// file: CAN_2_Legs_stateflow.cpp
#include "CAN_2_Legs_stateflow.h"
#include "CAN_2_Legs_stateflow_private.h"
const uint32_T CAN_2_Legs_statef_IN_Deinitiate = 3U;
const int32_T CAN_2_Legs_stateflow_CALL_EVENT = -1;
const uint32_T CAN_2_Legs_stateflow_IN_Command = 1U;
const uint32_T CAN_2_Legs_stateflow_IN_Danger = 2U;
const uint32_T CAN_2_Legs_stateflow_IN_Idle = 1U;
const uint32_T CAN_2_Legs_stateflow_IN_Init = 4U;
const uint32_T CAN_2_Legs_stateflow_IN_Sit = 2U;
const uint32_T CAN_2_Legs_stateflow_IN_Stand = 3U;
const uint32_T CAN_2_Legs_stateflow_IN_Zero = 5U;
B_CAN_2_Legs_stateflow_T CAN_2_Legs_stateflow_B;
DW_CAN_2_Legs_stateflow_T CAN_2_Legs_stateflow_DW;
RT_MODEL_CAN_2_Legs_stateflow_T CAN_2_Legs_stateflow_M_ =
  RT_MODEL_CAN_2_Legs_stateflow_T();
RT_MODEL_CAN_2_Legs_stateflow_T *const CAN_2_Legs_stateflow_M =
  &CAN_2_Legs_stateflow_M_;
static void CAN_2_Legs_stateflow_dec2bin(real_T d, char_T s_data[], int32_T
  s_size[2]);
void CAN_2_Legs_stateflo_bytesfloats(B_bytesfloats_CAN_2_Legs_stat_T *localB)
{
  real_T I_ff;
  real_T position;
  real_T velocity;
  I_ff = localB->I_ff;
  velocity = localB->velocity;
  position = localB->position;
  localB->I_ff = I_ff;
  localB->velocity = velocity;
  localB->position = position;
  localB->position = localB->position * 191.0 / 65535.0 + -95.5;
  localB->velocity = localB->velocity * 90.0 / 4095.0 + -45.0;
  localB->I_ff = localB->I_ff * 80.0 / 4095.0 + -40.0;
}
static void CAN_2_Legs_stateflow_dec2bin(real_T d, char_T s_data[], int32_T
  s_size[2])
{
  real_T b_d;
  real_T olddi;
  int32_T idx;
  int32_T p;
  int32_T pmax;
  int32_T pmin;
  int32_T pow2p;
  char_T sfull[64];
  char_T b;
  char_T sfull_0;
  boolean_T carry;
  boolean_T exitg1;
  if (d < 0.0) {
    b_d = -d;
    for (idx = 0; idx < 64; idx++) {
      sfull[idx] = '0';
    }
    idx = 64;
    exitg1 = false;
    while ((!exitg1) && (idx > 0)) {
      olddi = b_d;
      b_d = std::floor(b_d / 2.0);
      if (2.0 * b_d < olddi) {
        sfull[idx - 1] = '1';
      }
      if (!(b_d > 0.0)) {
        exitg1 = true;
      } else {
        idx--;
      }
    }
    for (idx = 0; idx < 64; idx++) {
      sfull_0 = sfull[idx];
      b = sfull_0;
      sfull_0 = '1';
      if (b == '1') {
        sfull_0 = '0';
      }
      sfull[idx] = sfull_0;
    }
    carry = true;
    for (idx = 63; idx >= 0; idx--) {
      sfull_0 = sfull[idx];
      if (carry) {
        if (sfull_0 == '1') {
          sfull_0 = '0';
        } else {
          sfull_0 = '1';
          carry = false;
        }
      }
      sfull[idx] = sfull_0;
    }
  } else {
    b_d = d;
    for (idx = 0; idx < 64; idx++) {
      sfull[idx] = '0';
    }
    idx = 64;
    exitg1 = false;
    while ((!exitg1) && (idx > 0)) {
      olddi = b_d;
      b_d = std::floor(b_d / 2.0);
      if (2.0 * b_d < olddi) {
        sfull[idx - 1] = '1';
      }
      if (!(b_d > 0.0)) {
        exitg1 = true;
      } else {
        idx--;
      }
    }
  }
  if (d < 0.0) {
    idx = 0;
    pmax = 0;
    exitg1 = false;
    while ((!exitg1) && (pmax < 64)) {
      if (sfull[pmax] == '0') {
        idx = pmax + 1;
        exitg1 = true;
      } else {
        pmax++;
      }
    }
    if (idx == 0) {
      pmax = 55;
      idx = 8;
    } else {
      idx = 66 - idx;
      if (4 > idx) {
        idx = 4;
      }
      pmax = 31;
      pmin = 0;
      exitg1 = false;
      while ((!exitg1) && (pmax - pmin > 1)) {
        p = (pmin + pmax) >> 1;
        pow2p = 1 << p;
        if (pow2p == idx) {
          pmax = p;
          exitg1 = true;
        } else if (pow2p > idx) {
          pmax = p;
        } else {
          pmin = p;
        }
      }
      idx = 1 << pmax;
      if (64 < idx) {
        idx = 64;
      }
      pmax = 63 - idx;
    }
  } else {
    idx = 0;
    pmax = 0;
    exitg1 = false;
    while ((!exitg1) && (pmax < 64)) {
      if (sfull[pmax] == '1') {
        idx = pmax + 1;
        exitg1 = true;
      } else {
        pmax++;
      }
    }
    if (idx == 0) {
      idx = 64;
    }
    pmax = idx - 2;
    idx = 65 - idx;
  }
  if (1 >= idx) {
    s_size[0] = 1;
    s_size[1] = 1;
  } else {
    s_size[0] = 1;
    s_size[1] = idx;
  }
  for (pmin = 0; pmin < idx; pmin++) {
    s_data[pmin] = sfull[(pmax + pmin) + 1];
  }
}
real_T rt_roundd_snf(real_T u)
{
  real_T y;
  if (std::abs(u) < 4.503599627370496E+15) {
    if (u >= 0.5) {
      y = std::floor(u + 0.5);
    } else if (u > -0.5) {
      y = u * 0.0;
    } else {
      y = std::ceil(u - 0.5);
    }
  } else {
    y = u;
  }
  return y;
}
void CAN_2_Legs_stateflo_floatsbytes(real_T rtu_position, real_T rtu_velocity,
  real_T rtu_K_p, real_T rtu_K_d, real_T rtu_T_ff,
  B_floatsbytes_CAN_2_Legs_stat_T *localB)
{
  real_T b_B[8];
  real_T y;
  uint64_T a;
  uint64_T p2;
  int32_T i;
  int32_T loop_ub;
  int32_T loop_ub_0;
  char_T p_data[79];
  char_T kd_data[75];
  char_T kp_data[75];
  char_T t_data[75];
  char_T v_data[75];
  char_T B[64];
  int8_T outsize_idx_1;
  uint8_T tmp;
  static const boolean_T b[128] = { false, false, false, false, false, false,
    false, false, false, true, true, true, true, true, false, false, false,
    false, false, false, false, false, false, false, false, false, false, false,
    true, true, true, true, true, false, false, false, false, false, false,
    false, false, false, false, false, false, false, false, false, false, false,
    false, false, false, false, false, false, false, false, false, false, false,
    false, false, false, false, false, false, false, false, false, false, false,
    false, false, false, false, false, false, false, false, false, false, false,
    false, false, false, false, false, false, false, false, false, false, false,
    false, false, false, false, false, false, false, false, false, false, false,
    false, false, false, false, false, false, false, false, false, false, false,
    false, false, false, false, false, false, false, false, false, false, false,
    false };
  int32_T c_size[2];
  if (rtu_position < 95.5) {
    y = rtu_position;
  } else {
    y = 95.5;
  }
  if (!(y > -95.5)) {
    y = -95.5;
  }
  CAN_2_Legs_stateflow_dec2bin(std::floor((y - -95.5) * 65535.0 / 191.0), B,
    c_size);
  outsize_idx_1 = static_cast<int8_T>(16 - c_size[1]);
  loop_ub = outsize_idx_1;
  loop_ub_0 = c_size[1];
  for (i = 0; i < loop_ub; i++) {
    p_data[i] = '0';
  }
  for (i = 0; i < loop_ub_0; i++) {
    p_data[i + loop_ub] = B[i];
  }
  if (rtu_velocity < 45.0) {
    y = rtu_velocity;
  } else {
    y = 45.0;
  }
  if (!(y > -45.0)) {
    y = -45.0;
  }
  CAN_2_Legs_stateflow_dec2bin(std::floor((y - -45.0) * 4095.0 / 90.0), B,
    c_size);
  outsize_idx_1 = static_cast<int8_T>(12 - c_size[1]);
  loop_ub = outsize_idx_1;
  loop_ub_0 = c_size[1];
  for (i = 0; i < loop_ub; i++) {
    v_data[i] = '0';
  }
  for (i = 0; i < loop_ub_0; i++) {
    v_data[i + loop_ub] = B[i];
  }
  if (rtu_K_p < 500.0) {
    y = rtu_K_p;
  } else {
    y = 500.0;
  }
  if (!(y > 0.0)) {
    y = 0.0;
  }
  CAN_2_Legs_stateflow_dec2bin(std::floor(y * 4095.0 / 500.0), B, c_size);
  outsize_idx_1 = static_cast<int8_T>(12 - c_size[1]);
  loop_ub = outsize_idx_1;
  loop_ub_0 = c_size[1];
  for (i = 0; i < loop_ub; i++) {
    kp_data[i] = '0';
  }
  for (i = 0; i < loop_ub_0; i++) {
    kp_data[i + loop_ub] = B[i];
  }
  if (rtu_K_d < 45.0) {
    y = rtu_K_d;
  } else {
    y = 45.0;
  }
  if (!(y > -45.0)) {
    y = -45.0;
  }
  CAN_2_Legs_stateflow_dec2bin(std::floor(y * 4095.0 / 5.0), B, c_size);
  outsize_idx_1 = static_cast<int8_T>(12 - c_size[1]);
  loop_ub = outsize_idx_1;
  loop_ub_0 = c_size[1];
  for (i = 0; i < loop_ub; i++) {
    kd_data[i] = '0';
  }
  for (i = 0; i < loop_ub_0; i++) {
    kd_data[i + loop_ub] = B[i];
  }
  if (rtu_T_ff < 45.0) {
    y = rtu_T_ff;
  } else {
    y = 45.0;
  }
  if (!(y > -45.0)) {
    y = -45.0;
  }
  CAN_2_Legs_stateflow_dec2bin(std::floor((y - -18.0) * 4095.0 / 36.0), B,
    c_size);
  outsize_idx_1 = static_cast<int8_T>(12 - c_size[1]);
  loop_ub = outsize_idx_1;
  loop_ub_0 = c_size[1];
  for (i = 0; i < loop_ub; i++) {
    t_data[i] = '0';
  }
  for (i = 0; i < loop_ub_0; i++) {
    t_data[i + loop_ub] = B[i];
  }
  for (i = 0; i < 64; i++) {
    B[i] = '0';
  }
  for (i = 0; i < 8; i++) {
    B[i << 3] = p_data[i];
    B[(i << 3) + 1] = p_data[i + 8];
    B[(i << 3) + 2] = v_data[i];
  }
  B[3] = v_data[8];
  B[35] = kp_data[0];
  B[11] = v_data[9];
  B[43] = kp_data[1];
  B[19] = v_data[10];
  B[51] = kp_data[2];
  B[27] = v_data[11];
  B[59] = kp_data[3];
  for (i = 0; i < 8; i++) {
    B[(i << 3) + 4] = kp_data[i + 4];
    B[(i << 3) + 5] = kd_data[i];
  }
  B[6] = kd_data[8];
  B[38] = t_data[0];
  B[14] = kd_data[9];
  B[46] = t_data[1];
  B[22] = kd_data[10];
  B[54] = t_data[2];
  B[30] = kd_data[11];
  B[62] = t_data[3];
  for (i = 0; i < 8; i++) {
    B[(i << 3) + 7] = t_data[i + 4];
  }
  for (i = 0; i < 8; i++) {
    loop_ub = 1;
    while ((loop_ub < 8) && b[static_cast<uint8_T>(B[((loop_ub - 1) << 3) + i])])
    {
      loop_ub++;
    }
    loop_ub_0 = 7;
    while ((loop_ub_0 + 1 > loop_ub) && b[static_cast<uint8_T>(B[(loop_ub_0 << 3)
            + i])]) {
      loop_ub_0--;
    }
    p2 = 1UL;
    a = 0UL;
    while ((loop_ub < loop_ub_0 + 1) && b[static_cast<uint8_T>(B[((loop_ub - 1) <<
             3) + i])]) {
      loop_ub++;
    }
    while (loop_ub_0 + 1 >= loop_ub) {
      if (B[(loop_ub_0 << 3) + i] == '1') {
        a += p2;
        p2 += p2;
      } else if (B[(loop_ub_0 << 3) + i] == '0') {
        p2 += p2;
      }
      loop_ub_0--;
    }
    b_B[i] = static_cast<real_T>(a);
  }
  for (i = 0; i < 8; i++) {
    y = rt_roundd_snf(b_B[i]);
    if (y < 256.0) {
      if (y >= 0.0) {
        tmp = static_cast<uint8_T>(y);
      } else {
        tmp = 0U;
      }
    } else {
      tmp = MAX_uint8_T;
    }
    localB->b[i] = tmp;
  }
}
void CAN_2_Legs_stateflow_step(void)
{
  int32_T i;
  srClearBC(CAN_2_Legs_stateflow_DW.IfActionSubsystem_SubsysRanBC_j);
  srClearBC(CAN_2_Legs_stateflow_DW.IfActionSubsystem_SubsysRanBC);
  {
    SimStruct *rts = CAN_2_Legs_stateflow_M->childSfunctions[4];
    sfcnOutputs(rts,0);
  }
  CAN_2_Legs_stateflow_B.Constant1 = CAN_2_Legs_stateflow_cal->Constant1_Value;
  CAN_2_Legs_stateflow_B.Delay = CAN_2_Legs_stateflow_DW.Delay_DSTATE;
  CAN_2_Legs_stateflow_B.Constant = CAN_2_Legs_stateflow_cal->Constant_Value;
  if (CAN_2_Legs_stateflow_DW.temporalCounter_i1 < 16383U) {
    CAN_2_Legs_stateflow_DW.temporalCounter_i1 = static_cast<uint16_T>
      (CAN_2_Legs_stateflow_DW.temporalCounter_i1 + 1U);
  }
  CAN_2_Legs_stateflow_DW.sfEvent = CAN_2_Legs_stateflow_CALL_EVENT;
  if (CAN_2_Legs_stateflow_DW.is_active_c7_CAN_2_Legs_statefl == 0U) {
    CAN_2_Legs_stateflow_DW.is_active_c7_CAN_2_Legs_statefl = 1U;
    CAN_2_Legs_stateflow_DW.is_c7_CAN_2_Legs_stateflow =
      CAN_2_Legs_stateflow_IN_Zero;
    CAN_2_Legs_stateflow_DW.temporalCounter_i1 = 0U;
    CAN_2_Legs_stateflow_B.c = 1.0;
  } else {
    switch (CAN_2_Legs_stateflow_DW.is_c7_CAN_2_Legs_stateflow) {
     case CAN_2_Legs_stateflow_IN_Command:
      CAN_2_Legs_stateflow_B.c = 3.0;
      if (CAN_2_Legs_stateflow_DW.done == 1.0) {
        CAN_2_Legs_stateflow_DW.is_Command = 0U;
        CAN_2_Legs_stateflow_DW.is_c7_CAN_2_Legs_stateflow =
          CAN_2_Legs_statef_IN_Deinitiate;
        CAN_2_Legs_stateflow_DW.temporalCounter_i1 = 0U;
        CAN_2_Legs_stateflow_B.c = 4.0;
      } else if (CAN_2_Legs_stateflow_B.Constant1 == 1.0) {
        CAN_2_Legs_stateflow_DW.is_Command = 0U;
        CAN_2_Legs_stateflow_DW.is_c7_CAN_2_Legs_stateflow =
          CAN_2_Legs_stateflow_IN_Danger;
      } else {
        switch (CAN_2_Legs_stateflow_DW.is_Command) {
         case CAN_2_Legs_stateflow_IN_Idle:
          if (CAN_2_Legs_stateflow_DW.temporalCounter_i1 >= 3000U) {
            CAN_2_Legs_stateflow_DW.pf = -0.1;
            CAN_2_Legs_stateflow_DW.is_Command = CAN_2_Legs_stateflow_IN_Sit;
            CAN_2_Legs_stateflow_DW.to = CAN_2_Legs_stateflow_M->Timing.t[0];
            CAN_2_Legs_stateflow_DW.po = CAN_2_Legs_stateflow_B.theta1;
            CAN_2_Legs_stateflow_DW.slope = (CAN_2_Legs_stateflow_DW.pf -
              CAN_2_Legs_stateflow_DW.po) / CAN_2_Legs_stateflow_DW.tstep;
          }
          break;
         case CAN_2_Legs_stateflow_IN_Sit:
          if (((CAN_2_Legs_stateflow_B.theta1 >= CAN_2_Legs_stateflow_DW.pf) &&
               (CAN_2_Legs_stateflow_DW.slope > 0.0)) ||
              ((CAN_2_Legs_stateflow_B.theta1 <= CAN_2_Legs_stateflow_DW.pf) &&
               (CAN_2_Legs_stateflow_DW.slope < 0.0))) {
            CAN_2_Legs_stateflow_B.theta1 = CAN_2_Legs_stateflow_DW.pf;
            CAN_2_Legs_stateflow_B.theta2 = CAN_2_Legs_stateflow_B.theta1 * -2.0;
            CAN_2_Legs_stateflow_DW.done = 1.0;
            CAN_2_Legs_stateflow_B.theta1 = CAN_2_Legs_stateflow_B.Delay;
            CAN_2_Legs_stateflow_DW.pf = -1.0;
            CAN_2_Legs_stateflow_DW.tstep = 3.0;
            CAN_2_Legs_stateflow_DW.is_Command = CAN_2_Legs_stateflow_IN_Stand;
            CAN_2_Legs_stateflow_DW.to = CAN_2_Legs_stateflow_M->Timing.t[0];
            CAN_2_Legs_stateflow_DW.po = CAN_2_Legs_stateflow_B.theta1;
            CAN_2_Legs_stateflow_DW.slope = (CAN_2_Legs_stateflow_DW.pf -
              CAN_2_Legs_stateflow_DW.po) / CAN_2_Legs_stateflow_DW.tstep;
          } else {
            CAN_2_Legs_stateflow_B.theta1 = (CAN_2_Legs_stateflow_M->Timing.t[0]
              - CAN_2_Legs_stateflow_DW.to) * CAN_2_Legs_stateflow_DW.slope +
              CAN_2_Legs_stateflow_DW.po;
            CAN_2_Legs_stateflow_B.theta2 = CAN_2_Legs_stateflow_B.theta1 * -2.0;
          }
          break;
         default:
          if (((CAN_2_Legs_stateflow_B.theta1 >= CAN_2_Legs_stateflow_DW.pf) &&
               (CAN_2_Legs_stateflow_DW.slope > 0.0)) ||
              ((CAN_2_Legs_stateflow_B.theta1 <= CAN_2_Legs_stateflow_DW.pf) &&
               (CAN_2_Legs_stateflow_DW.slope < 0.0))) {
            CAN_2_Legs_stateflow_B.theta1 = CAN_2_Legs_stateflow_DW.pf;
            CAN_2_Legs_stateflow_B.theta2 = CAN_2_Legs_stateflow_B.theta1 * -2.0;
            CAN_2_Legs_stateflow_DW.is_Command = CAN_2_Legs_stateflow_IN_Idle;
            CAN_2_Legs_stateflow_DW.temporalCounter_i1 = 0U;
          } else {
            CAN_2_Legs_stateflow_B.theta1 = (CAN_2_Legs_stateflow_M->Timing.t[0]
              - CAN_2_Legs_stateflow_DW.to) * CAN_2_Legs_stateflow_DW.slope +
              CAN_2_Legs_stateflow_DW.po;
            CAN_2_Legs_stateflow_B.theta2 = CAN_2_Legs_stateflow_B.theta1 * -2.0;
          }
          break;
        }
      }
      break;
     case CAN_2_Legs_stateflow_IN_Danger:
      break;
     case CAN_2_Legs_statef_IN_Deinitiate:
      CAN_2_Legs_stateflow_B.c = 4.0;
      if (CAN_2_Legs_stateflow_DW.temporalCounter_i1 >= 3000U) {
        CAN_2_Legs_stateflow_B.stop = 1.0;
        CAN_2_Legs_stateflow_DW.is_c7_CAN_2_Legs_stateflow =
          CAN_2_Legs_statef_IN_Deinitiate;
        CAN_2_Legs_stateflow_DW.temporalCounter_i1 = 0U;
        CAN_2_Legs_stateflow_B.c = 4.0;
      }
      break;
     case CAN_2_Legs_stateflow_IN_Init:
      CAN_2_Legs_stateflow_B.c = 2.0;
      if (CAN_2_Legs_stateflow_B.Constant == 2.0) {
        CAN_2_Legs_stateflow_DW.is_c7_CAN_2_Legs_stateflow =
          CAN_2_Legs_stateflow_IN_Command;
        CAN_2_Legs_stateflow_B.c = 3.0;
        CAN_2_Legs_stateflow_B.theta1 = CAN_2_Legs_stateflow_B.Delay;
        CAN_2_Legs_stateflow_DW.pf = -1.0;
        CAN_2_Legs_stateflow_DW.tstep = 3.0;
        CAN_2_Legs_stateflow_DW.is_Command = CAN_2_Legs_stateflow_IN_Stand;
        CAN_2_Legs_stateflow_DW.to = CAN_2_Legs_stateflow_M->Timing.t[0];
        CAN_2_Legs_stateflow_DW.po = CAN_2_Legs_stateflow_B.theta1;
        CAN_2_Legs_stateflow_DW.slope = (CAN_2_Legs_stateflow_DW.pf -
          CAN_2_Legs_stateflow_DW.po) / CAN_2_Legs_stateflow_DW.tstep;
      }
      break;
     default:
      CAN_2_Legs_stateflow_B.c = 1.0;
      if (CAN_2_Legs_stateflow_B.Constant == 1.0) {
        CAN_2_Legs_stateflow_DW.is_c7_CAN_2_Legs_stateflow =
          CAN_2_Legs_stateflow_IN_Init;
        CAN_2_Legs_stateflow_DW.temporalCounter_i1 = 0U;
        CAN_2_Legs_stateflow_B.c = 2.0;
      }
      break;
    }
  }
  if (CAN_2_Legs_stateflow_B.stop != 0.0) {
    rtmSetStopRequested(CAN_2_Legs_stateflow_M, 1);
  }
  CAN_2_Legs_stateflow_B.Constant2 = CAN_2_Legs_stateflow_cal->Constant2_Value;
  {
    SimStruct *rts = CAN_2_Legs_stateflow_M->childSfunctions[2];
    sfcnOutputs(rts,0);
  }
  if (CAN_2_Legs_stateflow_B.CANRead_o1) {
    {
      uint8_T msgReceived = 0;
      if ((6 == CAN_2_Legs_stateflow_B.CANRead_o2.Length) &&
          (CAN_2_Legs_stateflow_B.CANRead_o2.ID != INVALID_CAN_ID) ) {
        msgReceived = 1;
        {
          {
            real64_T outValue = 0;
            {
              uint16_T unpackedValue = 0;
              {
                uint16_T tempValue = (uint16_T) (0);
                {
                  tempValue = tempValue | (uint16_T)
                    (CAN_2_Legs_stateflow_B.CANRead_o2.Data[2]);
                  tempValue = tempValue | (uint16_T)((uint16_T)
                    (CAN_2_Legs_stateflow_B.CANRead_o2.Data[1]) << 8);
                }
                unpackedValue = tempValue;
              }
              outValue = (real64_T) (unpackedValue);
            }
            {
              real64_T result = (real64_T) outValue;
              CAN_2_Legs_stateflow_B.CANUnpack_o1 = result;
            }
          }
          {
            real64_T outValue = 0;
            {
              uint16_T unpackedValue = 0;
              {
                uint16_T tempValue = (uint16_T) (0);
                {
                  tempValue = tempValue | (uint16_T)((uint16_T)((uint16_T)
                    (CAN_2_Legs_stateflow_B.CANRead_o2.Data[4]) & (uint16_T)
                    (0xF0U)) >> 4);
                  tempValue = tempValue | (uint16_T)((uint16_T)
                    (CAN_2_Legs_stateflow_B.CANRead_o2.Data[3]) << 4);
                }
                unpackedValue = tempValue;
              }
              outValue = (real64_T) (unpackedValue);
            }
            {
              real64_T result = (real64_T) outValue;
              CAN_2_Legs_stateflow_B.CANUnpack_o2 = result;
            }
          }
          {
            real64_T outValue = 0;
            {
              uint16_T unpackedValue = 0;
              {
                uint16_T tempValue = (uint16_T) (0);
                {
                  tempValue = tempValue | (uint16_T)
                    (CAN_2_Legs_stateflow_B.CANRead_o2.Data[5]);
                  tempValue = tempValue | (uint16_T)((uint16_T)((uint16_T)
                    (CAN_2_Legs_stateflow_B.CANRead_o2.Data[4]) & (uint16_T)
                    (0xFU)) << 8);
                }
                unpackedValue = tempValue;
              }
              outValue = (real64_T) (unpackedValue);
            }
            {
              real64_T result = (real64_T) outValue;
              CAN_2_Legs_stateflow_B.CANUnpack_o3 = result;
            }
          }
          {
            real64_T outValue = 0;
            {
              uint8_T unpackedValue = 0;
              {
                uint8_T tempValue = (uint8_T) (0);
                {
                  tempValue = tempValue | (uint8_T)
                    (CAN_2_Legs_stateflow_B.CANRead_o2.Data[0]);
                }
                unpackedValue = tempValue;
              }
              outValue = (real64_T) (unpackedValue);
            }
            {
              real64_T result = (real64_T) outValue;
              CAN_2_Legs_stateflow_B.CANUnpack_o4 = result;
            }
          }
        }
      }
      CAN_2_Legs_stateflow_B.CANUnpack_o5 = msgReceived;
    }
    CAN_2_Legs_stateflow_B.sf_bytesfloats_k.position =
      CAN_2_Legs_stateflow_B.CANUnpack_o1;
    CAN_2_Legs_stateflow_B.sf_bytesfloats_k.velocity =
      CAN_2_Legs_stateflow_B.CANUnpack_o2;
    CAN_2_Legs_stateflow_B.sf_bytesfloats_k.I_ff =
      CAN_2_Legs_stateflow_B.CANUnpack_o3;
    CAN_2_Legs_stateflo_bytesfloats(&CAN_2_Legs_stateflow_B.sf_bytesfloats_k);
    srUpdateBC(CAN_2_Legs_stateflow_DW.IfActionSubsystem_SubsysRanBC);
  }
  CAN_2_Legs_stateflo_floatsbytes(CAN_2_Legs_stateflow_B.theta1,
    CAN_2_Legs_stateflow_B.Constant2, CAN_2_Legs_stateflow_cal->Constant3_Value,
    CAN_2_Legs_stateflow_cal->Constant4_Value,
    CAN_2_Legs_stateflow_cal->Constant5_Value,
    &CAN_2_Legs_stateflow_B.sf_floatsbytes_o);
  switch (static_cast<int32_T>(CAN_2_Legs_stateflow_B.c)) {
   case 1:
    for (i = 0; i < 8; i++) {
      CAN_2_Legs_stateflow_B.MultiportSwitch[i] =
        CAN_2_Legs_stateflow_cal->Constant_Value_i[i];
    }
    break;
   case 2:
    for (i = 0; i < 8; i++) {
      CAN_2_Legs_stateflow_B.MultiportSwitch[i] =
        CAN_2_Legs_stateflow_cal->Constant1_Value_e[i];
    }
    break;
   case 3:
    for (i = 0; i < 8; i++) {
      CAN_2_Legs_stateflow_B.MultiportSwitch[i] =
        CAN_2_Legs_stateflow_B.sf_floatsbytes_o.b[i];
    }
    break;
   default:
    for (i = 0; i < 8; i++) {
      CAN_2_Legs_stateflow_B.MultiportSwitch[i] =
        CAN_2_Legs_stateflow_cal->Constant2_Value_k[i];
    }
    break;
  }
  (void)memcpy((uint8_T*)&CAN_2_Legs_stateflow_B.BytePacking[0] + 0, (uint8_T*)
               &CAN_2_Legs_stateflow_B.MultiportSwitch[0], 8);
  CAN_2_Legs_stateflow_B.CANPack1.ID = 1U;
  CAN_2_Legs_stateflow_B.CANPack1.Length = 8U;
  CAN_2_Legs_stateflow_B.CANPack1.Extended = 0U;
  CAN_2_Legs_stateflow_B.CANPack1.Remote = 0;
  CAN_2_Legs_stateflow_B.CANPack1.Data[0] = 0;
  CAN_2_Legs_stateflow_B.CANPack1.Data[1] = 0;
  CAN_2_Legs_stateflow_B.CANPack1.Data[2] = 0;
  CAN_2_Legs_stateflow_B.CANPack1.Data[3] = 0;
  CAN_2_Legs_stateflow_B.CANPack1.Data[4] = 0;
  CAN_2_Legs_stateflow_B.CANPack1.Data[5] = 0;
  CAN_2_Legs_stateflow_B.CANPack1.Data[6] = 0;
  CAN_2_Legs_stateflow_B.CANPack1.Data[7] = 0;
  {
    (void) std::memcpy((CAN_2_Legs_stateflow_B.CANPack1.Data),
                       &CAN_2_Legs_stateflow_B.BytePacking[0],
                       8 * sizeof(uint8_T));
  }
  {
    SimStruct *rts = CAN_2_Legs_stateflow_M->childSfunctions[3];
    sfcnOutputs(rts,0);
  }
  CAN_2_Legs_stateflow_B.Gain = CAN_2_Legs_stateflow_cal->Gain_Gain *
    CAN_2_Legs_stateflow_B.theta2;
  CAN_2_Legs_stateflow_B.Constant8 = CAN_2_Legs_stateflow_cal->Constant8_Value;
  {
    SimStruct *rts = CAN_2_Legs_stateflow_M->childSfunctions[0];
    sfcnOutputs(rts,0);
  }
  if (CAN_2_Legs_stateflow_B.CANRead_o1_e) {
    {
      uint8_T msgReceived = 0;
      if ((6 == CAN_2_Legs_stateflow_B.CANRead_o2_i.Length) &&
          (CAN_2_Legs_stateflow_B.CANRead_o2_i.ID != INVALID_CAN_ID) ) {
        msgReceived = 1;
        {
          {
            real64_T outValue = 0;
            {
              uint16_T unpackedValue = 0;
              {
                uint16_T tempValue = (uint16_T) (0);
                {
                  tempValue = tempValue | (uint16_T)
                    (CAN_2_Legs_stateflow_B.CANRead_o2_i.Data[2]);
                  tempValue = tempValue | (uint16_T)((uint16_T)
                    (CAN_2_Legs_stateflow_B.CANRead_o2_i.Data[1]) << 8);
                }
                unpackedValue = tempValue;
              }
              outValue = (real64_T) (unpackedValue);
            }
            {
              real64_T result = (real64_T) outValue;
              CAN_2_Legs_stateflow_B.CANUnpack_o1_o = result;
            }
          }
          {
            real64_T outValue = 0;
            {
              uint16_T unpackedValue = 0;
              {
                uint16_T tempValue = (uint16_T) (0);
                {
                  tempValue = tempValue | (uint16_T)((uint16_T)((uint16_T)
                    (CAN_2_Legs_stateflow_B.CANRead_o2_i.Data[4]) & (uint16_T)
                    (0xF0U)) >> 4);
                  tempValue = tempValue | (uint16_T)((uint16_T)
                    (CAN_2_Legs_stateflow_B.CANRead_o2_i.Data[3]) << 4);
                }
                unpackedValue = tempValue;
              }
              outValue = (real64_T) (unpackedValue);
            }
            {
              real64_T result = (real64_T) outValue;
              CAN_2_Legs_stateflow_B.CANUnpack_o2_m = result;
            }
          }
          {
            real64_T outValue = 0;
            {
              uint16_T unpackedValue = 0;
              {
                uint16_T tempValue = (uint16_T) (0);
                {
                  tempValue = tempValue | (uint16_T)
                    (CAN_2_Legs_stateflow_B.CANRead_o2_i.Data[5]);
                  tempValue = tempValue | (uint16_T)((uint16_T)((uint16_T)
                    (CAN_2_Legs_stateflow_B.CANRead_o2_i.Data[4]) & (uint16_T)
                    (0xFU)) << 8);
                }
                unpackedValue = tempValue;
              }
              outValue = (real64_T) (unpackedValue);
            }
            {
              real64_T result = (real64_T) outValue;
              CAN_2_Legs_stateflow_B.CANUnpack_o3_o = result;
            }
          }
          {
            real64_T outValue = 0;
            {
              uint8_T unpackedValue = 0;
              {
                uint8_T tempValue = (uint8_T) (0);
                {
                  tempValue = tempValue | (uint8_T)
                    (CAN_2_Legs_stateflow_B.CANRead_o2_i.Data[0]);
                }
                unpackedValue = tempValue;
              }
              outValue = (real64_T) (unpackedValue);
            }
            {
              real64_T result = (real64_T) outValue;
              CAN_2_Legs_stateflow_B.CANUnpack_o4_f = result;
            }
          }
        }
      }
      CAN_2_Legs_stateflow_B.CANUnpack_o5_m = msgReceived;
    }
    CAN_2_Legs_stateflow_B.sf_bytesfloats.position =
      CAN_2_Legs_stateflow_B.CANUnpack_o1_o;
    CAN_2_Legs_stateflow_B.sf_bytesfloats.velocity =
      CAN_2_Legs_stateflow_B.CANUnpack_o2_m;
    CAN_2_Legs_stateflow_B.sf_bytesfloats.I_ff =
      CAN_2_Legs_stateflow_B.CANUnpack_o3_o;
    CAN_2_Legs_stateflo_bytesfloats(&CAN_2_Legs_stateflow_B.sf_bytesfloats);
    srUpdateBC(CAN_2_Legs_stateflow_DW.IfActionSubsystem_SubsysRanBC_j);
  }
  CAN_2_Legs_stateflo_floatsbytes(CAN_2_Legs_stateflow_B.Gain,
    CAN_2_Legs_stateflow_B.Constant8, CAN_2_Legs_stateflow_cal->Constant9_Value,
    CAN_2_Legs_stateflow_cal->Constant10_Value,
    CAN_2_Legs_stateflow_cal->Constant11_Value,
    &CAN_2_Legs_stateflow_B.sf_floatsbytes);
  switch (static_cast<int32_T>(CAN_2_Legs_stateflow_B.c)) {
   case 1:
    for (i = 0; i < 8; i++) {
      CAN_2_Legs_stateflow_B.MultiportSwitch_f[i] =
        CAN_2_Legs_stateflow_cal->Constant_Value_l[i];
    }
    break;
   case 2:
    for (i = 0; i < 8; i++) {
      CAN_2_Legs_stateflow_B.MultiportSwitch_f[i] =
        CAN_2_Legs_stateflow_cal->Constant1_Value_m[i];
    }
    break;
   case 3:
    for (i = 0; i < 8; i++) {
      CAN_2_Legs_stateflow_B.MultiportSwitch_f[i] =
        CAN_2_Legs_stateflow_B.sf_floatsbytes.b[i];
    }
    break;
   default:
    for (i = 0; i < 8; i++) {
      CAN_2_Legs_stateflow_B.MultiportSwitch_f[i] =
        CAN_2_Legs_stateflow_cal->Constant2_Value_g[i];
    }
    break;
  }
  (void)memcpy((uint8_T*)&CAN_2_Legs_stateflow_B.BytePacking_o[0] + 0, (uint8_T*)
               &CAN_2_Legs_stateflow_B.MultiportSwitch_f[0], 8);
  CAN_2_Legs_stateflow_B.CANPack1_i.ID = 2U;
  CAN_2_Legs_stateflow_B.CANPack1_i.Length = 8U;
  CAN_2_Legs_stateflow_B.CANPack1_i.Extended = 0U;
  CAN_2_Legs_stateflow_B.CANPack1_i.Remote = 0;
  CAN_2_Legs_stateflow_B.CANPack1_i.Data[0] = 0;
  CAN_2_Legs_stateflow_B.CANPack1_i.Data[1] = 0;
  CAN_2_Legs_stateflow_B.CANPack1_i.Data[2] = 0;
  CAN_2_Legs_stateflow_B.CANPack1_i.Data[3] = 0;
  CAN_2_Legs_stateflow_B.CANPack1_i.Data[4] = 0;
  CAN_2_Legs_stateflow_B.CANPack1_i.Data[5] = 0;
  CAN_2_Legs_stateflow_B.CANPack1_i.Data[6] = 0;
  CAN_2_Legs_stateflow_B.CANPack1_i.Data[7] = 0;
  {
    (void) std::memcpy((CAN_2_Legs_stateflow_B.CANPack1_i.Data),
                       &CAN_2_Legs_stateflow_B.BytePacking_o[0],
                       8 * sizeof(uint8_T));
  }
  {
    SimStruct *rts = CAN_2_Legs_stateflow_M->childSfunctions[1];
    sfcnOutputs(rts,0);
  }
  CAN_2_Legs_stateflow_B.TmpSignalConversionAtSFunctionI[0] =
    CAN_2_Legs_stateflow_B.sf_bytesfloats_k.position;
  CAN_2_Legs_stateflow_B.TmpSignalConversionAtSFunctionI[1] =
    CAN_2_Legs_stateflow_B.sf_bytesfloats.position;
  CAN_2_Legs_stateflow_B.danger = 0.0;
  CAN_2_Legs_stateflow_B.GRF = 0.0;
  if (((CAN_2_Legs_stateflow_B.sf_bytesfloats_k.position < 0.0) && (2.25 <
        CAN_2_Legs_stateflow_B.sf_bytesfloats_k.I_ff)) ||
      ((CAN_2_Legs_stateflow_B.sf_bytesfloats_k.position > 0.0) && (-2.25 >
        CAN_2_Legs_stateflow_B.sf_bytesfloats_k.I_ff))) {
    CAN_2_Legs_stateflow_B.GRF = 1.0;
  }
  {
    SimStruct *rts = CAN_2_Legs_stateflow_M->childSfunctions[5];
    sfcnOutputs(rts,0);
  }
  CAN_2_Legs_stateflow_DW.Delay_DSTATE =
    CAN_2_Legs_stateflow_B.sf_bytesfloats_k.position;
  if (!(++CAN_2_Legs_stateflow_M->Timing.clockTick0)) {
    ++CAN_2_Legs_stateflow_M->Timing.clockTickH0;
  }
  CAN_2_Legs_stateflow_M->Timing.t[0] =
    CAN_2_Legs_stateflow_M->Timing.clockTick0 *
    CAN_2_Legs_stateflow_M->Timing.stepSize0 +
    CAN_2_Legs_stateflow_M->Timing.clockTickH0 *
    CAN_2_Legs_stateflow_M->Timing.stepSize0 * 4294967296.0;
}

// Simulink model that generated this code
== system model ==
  CANSetup#1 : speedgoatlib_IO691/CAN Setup
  Stop#1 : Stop  <- 1: Stateflowchart#1
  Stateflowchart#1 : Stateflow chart  <- 1: Constant1, 2: Delay, 3: Constant
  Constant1 : Constant  Value=0
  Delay : Delay  DelayLength=1  <- 1: Subsystem#1
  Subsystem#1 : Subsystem  <- 1: Stateflowchart#1/4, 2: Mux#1
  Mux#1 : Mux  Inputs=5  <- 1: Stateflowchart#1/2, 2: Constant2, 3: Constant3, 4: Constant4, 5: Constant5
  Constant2 : Constant  Value=0
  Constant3 : Constant  Value=6
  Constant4 : Constant  Value=0.1
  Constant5 : Constant  Value=0
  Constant : Constant  Value=0
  MATLABFunction#1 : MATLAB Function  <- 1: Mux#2
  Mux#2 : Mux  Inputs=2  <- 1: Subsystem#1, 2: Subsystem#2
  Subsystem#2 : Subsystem  <- 1: Stateflowchart#1/4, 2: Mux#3
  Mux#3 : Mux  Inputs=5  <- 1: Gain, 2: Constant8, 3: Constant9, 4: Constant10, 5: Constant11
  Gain : Gain  Gain=18/30  <- 1: Stateflowchart#1/3
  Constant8 : Constant  Value=0
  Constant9 : Constant  Value=10
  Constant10 : Constant  Value=0.1
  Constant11 : Constant  Value=0
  MATLABFunction#2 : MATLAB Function  <- 1: Subsystem#1/3, 2: Subsystem#1
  CANStatus#1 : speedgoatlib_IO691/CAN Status
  RotarySwitchBlock#1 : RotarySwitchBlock
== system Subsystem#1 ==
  Inport#1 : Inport
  Command : Inport
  Outport#1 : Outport  <- 1: IfActionSubsystem
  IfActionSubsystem : Subsystem  <- 1: CANRead/2, Action: If#1
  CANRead : speedgoatlib_IO691/CAN Read
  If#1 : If  IfExpression=u1 ~= 0  <- 1: CANRead
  Outport#2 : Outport  <- 1: IfActionSubsystem/2
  Outport#3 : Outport  <- 1: IfActionSubsystem/3
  ID : Outport  <- 1: IfActionSubsystem/4
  Outport#4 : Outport  <- 1: IfActionSubsystem/5
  CANWrite#1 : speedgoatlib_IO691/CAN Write  <- 1: CANPack1
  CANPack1 : canmsglib/CAN Pack  <- 1: BytePacking
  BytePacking : slrealtimeutilitieslib/Byte Packing  <- 1: MultiportSwitch
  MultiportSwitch : MultiPortSwitch  Inputs=4  <- 1: Inport#1, 2: Constant#1, 3: Constant#2, 4: floatsbytes, 5: Constant#3
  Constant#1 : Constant  Value=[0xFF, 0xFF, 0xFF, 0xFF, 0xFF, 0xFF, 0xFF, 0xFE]
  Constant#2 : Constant  Value=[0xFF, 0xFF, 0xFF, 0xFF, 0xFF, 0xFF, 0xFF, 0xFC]
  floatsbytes : MATLAB Function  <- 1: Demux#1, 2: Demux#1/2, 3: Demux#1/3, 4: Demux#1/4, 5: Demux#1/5
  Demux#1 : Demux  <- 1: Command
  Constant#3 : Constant  Value=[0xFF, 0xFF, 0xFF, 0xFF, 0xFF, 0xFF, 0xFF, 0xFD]
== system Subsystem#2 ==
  Inport#2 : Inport
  Inport#3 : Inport
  Outport#5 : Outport  <- 1: Subsystem#3
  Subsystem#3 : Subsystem  <- 1: CANRead#1/2, Action: If#2
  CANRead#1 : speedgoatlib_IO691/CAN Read
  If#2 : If  IfExpression=u1 ~= 0  <- 1: CANRead#1
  Outport#6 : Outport  <- 1: Subsystem#3/2
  Outport#7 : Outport  <- 1: Subsystem#3/3
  Outport#8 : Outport  <- 1: Subsystem#3/4
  Outport#9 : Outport  <- 1: Subsystem#3/5
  CANWrite#2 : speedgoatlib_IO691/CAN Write  <- 1: CANPack#1
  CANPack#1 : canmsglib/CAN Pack  <- 1: BytePacking#1
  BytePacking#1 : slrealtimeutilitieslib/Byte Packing  <- 1: MultiPortSwitch#1
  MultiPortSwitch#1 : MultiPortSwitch  Inputs=4  <- 1: Inport#2, 2: Constant#4, 3: Constant#5, 4: MATLABFunction#3, 5: Constant#6
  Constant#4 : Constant  Value=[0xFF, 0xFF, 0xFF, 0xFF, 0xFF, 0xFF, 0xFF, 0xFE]
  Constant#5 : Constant  Value=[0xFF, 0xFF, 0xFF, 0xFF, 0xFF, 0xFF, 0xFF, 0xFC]
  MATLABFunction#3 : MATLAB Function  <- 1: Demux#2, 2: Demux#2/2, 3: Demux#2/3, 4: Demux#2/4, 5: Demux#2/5
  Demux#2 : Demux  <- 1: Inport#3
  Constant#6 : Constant  Value=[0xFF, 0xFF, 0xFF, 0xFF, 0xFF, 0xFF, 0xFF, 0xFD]
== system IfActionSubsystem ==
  Inport#4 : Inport
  ActionPort#1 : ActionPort
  Outport#10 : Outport  <- 1: bytesfloats
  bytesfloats : MATLAB Function  <- 1: CANUnpack, 2: CANUnpack/2, 3: CANUnpack/3
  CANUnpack : canmsglib/CAN Unpack  <- 1: Inport#4
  Outport#11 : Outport  <- 1: bytesfloats/2
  Outport#12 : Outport  <- 1: bytesfloats/3
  Outport#13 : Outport  <- 1: CANUnpack/4
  Outport#14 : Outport  <- 1: CANUnpack/5
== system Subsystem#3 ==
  Inport#5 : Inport
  ActionPort#2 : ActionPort
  Outport#15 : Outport  <- 1: MATLABFunction#4
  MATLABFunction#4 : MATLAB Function  <- 1: CANUnpack#1, 2: CANUnpack#1/2, 3: CANUnpack#1/3
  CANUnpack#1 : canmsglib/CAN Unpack  <- 1: Inport#5
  Outport#16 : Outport  <- 1: MATLABFunction#4/2
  Outport#17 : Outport  <- 1: MATLABFunction#4/3
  Outport#18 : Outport  <- 1: CANUnpack#1/4
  Outport#19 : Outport  <- 1: CANUnpack#1/5
== matlab function MATLABFunction#2 ==
function GRF = isGRF(Iff, P1)
    GRF = 0;
    threshhold = 2.25;
    
    if((P1<0 && threshhold<Iff)|| (P1>0 && -threshhold>Iff))
        GRF = 1;
    end

== matlab function floats -> bytes ==
function b = fcn(position, velocity, K_p, K_d, T_ff)

P_MIN  =-95.5;  % [rad]
P_MAX  = 95.5;  % [rad]
V_MIN  =-45;    % [rad/s] 30 to 45
V_MAX  = 45;    % [rad/s]
KP_MIN = 0;     % [Nm/rad]
KP_MAX = 500;   % [Nm/rad]
KD_MIN = 0;     % [Nm*s/rad
KD_MAX = 5;     % [Nm*s/rad
T_MIN  =-18;    % [Nm]
T_MAX  = 18;    % [Nm]

position = floor((max(min(position,P_MAX) ,P_MIN)  - P_MIN )*65535/(P_MAX  - P_MIN));
velocity = floor((max(min(velocity,V_MAX) ,V_MIN)  - V_MIN )*4095 /(V_MAX  - V_MIN));
K_p      = floor((max(min(K_p     ,KP_MAX),KP_MIN) - KP_MIN)*4095 /(KP_MAX - KP_MIN));
K_d      = floor((max(min(K_d     ,V_MAX) ,V_MIN)  - KD_MIN)*4095 /(KD_MAX - KD_MIN));
T_ff     = floor((max(min(T_ff    ,V_MAX) ,V_MIN)  - T_MIN )*4095 /(T_MAX  - T_MIN));

p  = dec2bin(position);
p  = [repmat('0', 1, 16-length(p)),p];
v  = dec2bin(velocity);
v  = [repmat('0', 1, 12-length(v)),v];
kp = dec2bin(K_p);
kp  = [repmat('0', 1, 12-length(kp)),kp];
kd = dec2bin(K_d);
kd  = [repmat('0', 1, 12-length(kd)),kd];
t  = dec2bin(T_ff);
t  = [repmat('0', 1, 12-length(t)),t];

B = repmat('0', 8, 8);

B(1,:) = p(1:8);
B(2,:) = p(9:16);
B(3,:) = v(1:8);
B(4,:) = [v(9:12),kp(1:4)];
B(5,:) = kp(5:12);
B(6,:) = kd(1:8);
B(7,:) = [kd(9:12),t(1:4)];
B(8,:) = t(5:12);

B  = bin2dec(B);

b = uint8(B);

== matlab function MATLABFunction#1 ==
function danger = isDanger(Pmux)
    % Pmux position matrix radians
    %       [p(ID1),p(ID2),p(ID3),p(IDN)]
    
    p1Max = .5; 
    p1Min = -.5;
    p2Max = .5;
    p2Min = -.5;
    
    P1 = Pmux(1:2:end);
    P2 = Pmux(2:2:end);
    
    
    danger = 0;
    if((0<sum(P1>p1Max + P1<p1Min)) || (0<sum(P2>p2Max + P2<p2Min)))
        danger = 1;
    end

== stateflow chart Stateflowchart#1 ==
  state Zero
    entry:
    c = 1;
  state Init
    entry:
    c = 2;
  state Command
    entry:
    c = 3;
    state Stand
      entry:
      to = t;
      po = theta1;
      slope = (pf - po)/tstep
      during:
      theta1 = po + slope*(t-to);
      theta2 = theta1 * -2;
    state Flight [commented out]
    state Idle
    state Sit
      entry:
      to = t;
      po = theta1;
      slope = (pf - po)/tstep;
      during:
      theta1 = po + slope*(t-to);
      theta2 = theta1 * -2;
    (default) -> Stand : {theta1 = pc;
        | pf = -.1;
        | tstep = 3;}
    Stand -> Idle : [(theta1 >= pf & slope>0) | (theta1 <= pf & slope<0)]
        | {theta1 = pf; theta2 = theta1 * -2;}
    Flight -> Idle [commented out] : [GRFy > 0]
    Idle -> Flight [commented out] : [GRFy == 0]
    Idle -> Sit : after(3,sec)
        | {pf = -1;}
    Sit -> Command : [(theta1 >= pf & slope>0) | (theta1 <= pf & slope<0)]
        | {theta1 = pf; theta2 = theta1 * -2; done = 1;}
  state Danger
  state Deinitiate
    entry:
    c = 4;
  (default) -> Zero
  Zero -> Init : [isReady == 1]
      | {after(15,sec);}
  Init -> Command : [isReady == 2]
      | {after(3,sec);}
  Command -> Danger [order 2] : [danger == 1]
  Command -> Deinitiate [order 1] : [done == 1]
  (junction 36) -> Deinitiate : {stop = 1;}
  Deinitiate -> (junction 36) : after(3,sec)
  data: stop output =0; theta1 output; theta2 output; c output; done local =0; danger input; pc input; pf local; po local; slope local; tstep local; to local; isReady input

== matlab function floats -> bytes ==
function b = fcn(position, velocity, K_p, K_d, T_ff)

P_MIN  =-95.5;  % [rad]
P_MAX  = 95.5;  % [rad]
V_MIN  =-45;    % [rad/s] 30 to 45
V_MAX  = 45;    % [rad/s]
KP_MIN = 0;     % [Nm/rad]
KP_MAX = 500;   % [Nm/rad]
KD_MIN = 0;     % [Nm*s/rad
KD_MAX = 5;     % [Nm*s/rad
T_MIN  =-18;    % [Nm]
T_MAX  = 18;    % [Nm]

position = floor((max(min(position,P_MAX) ,P_MIN)  - P_MIN )*65535/(P_MAX  - P_MIN));
velocity = floor((max(min(velocity,V_MAX) ,V_MIN)  - V_MIN )*4095 /(V_MAX  - V_MIN));
K_p      = floor((max(min(K_p     ,KP_MAX),KP_MIN) - KP_MIN)*4095 /(KP_MAX - KP_MIN));
K_d      = floor((max(min(K_d     ,V_MAX) ,V_MIN)  - KD_MIN)*4095 /(KD_MAX - KD_MIN));
T_ff     = floor((max(min(T_ff    ,V_MAX) ,V_MIN)  - T_MIN )*4095 /(T_MAX  - T_MIN));

p  = dec2bin(position);
p  = [repmat('0', 1, 16-length(p)),p];
v  = dec2bin(velocity);
v  = [repmat('0', 1, 12-length(v)),v];
kp = dec2bin(K_p);
kp  = [repmat('0', 1, 12-length(kp)),kp];
kd = dec2bin(K_d);
kd  = [repmat('0', 1, 12-length(kd)),kd];
t  = dec2bin(T_ff);
t  = [repmat('0', 1, 12-length(t)),t];

B = repmat('0', 8, 8);

B(1,:) = p(1:8);
B(2,:) = p(9:16);
B(3,:) = v(1:8);
B(4,:) = [v(9:12),kp(1:4)];
B(5,:) = kp(5:12);
B(6,:) = kd(1:8);
B(7,:) = [kd(9:12),t(1:4)];
B(8,:) = t(5:12);

B  = bin2dec(B);

b = uint8(B);
